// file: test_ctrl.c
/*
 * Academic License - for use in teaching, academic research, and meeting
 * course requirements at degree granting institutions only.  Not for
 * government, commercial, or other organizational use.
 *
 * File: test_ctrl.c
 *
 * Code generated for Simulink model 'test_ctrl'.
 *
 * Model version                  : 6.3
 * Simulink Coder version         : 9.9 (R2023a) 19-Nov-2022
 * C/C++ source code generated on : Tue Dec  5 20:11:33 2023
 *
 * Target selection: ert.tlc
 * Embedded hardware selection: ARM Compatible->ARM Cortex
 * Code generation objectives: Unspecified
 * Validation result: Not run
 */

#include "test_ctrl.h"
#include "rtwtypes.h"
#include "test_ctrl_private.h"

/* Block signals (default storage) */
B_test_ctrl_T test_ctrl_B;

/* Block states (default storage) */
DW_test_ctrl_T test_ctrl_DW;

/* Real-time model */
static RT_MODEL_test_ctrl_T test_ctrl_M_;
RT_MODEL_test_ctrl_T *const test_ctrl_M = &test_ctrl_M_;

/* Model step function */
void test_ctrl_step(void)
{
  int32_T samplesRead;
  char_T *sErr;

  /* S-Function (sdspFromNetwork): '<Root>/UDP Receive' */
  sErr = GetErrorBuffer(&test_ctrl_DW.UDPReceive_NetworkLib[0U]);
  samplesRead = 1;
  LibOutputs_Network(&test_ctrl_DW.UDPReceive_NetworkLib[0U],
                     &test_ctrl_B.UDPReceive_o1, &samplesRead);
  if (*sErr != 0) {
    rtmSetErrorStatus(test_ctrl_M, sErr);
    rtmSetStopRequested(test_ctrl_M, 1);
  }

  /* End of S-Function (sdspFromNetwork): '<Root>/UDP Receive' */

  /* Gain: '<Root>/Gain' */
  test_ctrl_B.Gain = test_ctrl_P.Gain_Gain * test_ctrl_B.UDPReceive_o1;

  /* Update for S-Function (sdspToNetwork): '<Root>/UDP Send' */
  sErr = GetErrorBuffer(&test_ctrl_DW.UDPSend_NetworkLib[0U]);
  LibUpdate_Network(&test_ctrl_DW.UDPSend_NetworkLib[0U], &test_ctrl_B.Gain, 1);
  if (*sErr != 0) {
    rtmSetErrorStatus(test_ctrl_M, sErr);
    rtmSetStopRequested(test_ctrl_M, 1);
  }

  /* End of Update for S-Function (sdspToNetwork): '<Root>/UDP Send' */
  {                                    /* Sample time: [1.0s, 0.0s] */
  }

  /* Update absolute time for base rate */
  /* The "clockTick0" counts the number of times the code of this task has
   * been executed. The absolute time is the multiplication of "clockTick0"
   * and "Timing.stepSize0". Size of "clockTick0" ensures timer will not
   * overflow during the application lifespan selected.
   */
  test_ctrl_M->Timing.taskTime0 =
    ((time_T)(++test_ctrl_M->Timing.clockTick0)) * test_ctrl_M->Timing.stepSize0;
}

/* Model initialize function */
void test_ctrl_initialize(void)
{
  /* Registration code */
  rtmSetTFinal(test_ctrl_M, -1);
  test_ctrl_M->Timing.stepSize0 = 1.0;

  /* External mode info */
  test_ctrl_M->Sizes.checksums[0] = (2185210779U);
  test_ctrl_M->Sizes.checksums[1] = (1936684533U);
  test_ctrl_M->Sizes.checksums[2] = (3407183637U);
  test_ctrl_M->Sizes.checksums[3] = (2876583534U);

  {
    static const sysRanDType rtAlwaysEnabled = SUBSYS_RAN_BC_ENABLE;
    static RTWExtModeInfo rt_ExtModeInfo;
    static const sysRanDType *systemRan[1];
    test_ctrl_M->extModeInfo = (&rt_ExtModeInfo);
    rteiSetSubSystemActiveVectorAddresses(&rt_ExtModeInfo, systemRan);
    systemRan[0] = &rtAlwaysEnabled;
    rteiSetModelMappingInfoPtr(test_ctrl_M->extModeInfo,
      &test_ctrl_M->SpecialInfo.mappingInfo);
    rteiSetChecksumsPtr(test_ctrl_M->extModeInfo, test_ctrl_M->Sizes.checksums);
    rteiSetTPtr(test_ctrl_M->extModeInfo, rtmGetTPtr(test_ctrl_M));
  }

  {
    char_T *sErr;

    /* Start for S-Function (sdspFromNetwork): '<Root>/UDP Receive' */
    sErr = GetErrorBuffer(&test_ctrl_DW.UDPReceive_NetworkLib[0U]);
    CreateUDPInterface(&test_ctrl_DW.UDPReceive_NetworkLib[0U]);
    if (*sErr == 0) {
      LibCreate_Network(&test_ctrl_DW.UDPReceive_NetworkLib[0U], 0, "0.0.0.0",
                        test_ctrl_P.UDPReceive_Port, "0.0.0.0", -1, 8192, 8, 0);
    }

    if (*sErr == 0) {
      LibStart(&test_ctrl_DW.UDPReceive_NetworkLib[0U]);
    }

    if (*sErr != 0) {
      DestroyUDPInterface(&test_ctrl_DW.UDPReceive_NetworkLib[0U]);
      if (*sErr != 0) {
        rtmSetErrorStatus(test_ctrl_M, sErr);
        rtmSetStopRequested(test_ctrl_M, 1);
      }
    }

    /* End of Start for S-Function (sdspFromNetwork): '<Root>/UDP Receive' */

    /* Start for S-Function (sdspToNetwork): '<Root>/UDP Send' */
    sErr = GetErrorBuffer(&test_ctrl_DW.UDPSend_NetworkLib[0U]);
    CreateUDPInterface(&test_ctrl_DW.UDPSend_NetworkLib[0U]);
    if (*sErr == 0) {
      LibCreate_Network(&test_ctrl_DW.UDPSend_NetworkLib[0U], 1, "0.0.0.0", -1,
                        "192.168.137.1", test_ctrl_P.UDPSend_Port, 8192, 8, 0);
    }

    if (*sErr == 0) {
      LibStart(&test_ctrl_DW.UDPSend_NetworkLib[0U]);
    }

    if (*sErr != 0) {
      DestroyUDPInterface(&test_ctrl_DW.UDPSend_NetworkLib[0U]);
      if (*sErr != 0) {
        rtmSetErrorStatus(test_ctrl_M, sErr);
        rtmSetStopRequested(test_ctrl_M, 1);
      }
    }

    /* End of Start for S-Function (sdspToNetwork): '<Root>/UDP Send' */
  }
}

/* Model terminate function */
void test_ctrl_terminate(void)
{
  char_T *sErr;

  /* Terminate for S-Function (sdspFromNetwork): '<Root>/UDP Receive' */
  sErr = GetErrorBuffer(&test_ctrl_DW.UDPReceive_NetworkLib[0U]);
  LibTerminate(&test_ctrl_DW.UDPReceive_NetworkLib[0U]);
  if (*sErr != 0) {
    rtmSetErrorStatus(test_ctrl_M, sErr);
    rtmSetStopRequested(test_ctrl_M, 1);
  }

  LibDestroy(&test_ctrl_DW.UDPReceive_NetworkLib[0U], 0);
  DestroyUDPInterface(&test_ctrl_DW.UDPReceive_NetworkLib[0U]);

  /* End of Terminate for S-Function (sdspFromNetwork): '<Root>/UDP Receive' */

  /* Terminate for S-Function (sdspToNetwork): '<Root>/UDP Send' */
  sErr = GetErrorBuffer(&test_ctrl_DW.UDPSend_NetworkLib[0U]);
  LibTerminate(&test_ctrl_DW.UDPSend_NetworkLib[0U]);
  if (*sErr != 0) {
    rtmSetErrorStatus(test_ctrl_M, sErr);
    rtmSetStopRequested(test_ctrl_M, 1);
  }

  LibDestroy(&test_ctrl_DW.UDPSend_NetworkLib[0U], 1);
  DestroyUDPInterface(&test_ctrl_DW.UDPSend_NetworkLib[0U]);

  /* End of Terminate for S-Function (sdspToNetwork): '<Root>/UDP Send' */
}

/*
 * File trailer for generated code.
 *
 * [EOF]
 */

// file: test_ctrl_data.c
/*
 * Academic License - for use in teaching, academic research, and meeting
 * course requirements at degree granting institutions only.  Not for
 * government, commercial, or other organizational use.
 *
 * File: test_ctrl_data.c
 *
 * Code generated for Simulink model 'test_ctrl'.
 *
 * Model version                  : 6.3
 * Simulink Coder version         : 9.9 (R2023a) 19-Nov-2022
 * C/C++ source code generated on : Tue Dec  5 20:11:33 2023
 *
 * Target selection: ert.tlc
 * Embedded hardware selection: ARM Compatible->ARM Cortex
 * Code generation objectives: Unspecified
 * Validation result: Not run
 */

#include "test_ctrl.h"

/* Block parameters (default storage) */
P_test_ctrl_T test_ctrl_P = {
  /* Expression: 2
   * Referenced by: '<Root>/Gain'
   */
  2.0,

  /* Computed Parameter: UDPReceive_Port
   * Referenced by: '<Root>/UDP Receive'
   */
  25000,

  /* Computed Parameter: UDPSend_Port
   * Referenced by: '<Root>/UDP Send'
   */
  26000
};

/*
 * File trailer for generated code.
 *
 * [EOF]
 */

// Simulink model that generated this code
simulink model "test_ctrl"  (R2023a)
settings: Solver=FixedStepAuto  StartTime=0.0  StopTime=Inf  RelTol=1e-3  EnableMultiTasking=on
libraries: embedlinuxNetworklib x2

== system test_ctrl ==
  Gain : Gain  Gain=2
  Scope2 : Scope
  Terminator : Terminator
  UDP Receive : embedlinuxNetworklib/UDP Receive  localURL='0.0.0.0'  localPort=25000  remoteURL='0.0.0.0'  remotePort=-1  recvBufferSize=8192  signalDatatype=double  dims=1  isVarSize=off  showBlockingTime=off  blockingTime=0  sampletime=1.0  blockPlatform=Raspberry Pi
  UDP Send : embedlinuxNetworklib/UDP Send  remoteURL='192.168.137.1'  remotePort=26000  localURL='0.0.0.0'  localPortSource=Automatically determine  localPort=-1  sampletime=-1  blockPlatform=Raspberry Pi  separateLengthPort=0
  Scope1 : Scope
  wires:
  Gain/1 -> Scope2/1, UDP Send/1
  UDP Receive/2 -> Terminator/1
  UDP Receive/1 -> Gain/1
